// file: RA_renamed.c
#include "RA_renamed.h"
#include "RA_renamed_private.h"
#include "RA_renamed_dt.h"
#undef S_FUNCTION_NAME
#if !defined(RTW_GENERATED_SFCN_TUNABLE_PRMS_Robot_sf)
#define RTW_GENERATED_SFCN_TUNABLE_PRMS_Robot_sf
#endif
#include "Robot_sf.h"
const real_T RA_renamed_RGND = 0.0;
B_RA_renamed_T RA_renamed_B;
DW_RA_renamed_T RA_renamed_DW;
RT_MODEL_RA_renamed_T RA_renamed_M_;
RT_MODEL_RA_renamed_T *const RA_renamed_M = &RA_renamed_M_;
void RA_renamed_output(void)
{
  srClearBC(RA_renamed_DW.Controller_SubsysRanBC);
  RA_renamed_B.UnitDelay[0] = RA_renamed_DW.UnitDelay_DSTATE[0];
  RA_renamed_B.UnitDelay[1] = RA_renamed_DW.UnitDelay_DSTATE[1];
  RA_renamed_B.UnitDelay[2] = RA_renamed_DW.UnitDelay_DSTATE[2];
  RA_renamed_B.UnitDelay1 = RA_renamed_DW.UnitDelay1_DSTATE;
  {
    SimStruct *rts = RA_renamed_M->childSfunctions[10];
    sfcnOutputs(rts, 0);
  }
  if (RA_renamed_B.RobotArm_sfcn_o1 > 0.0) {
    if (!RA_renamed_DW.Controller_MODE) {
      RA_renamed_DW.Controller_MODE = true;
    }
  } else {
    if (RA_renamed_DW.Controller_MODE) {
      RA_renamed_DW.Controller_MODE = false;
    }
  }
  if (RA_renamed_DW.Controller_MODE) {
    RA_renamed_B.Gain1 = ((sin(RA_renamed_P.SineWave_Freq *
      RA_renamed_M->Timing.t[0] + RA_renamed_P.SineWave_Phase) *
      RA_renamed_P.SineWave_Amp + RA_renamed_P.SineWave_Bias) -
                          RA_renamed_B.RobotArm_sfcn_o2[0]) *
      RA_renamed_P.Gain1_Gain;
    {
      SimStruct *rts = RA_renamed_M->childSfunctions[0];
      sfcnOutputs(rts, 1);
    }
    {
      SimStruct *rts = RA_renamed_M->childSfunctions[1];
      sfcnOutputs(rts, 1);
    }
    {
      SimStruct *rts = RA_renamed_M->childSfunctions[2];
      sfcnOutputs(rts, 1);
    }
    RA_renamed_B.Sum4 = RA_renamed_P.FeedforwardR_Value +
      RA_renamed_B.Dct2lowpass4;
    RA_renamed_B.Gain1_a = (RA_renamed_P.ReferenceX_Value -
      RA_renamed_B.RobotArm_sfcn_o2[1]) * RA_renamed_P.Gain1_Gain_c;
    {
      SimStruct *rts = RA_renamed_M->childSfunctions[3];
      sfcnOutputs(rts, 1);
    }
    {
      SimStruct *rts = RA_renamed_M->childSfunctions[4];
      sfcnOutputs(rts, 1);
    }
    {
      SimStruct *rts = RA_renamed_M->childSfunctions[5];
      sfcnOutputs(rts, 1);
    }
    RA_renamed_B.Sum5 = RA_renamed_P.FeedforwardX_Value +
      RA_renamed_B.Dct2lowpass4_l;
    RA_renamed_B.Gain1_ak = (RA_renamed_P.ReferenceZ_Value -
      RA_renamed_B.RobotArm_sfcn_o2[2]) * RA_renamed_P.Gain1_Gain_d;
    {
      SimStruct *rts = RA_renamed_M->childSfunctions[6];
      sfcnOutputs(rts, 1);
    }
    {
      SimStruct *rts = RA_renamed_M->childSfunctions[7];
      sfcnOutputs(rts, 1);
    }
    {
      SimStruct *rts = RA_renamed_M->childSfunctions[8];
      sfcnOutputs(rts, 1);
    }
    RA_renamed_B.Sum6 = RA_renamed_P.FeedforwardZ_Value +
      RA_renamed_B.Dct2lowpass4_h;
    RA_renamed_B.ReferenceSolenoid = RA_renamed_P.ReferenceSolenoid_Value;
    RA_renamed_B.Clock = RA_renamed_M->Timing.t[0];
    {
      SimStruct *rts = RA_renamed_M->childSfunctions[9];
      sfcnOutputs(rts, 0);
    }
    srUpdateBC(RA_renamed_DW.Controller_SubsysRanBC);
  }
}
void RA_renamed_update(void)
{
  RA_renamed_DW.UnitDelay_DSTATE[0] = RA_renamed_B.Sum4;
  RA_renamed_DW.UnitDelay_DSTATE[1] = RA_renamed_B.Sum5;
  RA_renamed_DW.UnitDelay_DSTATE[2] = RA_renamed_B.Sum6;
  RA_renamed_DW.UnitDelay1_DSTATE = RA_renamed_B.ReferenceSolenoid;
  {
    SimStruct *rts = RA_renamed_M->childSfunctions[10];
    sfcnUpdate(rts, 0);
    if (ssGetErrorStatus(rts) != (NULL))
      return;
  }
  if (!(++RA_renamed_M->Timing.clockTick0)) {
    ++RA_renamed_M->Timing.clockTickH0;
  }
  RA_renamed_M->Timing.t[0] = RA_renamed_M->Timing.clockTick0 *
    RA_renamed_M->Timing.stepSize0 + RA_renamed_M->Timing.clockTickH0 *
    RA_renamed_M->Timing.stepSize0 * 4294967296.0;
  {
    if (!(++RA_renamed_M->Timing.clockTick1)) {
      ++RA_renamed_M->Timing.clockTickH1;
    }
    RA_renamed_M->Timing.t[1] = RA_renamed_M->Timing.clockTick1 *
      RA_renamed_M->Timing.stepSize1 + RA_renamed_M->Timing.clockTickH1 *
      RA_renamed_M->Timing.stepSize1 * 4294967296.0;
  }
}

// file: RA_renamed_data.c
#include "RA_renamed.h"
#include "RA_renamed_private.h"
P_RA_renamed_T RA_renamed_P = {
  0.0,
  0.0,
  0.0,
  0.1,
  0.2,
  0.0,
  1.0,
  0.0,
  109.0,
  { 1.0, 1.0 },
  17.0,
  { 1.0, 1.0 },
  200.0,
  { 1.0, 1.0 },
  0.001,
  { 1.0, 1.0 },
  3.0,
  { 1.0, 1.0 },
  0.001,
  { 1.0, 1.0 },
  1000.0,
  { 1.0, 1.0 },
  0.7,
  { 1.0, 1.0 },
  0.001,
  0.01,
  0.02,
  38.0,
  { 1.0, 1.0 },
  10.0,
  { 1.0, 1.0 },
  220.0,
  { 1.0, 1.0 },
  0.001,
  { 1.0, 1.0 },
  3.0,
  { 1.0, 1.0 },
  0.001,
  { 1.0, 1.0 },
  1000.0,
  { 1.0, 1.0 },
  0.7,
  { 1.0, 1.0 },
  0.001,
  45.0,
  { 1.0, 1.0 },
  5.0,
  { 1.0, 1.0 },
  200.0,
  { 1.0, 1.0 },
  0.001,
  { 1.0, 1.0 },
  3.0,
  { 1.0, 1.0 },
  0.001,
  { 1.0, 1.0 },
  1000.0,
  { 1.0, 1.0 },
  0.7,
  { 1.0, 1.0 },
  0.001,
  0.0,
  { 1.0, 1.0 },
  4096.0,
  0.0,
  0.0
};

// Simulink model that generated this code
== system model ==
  UnitDelay : UnitDelay  <- 1: Controller
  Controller : Subsystem  <- 1: RobotArm_sfcn/2, Enable: RobotArm_sfcn
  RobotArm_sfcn : S-Function  FunctionName=Robot_sf  <- 1: UnitDelay, 2: UnitDelay1
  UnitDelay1 : UnitDelay  <- 1: Controller/2
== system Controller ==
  Inport#1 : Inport
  EnablePort#1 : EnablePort
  Outport#1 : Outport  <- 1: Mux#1
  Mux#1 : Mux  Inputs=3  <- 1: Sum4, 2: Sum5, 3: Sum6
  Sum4 : Sum  Inputs=++  <- 1: FeedforwardR, 2: Dct2lowpass4
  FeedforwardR : Constant  Value=0
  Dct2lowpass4 : S-Function  FunctionName=dlowpass2  <- 1: SFunction#1
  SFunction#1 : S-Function  FunctionName=dweakint  <- 1: SFunction#2
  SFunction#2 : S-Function  FunctionName=dleadlag  <- 1: Gain1
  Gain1 : Gain  Gain=109  <- 1: Sum#1
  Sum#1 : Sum  Inputs=+-  <- 1: SineWave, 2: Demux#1
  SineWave : Sin  Amplitude=0.2
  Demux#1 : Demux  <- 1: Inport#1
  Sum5 : Sum  Inputs=++  <- 1: FeedforwardX, 2: SFunction#3
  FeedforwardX : Constant  Value=0
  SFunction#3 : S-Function  FunctionName=dlowpass2  <- 1: SFunction#4
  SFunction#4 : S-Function  FunctionName=dweakint  <- 1: SFunction#5
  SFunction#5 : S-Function  FunctionName=dleadlag  <- 1: Gain#1
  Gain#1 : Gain  Gain=38  <- 1: Sum#2
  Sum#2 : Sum  Inputs=+-  <- 1: ReferenceX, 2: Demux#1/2
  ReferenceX : Constant  Value=0.01
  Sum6 : Sum  Inputs=++  <- 1: FeedforwardZ, 2: SFunction#6
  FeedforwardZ : Constant  Value=0.1
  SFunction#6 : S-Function  FunctionName=dlowpass2  <- 1: SFunction#7
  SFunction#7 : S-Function  FunctionName=dweakint  <- 1: SFunction#8
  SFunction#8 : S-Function  FunctionName=dleadlag  <- 1: Gain#2
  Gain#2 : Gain  Gain=45  <- 1: Sum#3
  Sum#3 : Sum  Inputs=+-  <- 1: ReferenceZ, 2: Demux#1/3
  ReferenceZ : Constant  Value=0.02
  Outport#2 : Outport  InitialOutput=0  <- 1: ReferenceSolenoid
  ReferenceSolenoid : Constant  Value=0
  Clock : Clock
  SFunction#9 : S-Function  FunctionName=sf_rt_scope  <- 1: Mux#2
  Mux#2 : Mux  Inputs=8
